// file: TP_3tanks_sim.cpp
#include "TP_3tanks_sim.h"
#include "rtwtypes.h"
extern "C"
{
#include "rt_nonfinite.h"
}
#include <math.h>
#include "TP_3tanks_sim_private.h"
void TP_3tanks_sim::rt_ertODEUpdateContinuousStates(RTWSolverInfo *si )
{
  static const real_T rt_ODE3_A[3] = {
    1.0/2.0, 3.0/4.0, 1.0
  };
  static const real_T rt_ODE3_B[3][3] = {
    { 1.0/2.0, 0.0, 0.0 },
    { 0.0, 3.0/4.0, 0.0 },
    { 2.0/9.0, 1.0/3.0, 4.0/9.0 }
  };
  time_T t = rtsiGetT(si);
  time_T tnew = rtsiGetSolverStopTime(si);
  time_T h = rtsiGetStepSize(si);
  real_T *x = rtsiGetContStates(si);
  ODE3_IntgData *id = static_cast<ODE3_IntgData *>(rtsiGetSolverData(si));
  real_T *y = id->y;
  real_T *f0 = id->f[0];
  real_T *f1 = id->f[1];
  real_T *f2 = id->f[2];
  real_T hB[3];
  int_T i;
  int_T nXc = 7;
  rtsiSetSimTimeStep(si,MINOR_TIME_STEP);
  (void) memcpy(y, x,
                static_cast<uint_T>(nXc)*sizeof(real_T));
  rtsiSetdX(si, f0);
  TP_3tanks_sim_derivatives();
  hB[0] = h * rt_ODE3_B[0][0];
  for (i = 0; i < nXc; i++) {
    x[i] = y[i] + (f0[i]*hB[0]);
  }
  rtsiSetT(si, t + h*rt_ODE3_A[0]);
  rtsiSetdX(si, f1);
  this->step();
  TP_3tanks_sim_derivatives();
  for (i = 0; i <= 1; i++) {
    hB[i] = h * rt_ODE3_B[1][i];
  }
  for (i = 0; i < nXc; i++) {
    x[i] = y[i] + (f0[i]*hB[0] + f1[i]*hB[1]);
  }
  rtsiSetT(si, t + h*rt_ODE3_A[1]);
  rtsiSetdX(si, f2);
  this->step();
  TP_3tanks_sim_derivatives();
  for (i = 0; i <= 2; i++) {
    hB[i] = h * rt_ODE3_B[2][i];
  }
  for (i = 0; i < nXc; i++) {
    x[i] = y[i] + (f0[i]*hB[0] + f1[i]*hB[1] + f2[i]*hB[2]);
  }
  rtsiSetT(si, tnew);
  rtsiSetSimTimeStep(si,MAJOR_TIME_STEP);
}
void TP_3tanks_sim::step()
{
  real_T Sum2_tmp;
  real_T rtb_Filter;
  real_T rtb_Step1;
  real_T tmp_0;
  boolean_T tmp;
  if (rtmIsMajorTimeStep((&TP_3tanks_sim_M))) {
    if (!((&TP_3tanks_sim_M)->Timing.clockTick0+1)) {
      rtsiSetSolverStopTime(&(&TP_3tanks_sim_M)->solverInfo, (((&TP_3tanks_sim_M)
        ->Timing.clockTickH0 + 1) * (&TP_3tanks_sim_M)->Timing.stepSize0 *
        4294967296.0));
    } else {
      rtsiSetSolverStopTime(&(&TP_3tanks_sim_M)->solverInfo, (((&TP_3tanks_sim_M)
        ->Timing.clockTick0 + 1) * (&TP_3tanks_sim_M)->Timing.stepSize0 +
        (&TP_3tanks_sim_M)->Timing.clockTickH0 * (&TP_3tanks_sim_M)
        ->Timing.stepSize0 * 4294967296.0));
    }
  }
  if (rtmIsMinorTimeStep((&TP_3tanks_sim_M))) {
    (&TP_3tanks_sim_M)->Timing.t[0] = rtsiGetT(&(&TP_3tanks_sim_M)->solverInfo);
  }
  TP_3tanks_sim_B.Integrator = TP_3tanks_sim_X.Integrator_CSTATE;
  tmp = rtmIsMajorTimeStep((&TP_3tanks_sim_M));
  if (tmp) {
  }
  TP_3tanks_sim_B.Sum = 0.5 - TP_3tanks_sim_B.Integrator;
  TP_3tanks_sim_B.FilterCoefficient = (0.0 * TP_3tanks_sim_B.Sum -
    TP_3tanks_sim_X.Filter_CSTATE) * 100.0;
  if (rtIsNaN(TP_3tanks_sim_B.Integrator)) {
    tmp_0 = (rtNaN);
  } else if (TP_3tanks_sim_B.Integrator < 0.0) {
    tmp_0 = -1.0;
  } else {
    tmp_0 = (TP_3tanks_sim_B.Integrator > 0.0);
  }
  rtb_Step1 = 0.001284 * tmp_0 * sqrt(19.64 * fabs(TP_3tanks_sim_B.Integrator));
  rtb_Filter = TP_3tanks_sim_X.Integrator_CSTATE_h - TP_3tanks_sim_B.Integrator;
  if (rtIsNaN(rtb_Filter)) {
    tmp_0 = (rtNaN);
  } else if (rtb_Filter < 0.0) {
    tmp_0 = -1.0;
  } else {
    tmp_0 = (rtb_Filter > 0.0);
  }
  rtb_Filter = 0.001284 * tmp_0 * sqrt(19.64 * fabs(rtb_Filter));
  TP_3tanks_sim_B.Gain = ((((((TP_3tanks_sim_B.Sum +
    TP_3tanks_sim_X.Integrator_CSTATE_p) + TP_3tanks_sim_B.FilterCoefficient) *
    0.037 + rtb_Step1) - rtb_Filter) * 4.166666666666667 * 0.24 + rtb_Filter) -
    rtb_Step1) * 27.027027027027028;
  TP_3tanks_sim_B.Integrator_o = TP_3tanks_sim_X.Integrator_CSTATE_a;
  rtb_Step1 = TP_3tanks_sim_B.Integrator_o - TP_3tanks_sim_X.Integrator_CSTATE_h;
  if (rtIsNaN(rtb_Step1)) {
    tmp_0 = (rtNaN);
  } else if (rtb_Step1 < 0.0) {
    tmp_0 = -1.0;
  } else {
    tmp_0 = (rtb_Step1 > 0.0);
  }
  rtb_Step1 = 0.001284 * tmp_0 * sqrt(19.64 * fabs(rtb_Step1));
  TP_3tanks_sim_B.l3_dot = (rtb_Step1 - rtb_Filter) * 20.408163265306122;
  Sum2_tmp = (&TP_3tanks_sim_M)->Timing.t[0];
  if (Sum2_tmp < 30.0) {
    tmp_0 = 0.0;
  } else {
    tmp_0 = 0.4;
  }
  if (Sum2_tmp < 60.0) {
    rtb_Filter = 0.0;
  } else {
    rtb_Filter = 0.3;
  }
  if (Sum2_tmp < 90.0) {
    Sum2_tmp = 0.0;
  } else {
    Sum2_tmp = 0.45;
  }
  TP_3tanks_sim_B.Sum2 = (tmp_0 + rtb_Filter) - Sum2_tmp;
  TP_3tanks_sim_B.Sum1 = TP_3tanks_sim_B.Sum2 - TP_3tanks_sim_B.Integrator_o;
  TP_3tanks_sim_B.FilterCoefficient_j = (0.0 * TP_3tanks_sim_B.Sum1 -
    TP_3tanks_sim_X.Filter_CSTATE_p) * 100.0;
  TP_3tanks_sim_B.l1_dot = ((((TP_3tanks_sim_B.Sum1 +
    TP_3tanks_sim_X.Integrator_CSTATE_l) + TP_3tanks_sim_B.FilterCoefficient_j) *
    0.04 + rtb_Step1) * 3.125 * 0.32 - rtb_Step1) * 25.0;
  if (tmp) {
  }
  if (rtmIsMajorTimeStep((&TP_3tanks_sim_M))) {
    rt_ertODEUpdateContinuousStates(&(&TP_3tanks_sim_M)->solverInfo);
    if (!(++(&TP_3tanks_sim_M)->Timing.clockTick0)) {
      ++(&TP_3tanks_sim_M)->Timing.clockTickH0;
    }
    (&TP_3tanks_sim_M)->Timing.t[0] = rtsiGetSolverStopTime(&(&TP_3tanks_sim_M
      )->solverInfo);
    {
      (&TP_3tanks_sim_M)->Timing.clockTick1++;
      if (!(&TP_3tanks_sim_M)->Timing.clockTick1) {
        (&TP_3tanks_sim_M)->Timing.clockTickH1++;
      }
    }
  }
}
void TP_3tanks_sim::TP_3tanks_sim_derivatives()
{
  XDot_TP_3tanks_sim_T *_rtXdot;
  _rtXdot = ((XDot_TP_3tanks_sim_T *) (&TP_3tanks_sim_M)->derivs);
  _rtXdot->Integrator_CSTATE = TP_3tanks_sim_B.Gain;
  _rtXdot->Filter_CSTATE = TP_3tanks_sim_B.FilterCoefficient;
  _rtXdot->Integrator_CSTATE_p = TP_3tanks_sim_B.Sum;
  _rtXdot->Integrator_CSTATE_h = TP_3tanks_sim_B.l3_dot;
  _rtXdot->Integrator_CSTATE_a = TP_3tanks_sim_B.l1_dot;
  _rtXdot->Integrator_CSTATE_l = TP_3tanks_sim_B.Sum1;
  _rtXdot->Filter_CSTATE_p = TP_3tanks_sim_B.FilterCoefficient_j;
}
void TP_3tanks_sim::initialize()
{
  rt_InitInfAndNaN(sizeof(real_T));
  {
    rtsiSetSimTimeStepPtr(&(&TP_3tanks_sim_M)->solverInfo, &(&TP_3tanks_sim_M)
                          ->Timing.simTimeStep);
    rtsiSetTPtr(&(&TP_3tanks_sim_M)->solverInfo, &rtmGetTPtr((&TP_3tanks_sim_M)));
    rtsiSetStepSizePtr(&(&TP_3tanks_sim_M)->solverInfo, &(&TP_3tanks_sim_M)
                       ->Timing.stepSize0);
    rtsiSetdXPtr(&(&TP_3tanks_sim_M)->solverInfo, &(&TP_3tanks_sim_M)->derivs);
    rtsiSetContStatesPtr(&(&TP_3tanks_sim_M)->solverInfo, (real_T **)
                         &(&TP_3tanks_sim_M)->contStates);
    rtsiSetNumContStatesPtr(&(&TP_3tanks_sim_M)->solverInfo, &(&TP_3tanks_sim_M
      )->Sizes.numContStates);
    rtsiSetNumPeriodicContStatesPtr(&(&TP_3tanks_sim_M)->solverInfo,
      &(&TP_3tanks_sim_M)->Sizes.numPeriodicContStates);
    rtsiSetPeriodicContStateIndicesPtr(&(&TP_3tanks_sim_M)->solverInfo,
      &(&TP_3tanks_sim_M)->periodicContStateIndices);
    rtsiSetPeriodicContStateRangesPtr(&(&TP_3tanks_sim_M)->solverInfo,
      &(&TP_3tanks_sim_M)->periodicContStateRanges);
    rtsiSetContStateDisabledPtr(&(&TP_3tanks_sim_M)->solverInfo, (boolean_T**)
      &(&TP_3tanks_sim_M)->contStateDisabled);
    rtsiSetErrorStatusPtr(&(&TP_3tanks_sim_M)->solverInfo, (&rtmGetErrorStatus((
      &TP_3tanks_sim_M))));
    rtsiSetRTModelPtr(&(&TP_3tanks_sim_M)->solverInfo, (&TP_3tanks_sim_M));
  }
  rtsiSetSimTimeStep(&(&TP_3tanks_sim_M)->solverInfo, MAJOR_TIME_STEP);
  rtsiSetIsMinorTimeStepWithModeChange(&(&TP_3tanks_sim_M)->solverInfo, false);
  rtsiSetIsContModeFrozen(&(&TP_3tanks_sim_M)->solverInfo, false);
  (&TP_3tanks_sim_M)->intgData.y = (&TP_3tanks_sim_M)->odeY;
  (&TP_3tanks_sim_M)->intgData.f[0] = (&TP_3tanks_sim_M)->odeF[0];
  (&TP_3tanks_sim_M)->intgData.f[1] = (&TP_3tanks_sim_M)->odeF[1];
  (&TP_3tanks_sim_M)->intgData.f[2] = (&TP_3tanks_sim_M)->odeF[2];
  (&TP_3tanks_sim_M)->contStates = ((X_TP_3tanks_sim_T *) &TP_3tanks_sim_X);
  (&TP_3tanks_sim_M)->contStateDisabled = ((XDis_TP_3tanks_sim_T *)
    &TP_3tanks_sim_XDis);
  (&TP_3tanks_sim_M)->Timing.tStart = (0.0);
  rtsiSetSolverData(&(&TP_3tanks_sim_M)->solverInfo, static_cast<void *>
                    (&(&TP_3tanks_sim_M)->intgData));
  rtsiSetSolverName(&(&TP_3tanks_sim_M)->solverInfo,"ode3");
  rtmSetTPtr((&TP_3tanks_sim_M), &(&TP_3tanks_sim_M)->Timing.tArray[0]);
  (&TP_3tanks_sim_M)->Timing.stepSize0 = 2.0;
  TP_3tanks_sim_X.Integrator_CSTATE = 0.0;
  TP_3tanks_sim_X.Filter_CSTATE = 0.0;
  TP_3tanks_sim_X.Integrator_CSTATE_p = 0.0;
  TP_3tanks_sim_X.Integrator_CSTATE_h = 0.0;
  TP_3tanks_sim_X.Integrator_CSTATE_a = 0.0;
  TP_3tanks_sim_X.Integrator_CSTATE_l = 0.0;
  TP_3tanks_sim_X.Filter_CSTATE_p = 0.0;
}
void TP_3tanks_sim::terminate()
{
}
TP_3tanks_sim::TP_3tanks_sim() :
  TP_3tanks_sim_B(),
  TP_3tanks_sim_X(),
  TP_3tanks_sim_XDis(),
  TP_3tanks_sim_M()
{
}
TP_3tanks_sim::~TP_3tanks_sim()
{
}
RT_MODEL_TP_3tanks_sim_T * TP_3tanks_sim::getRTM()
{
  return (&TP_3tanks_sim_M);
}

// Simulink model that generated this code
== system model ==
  Integrator : Integrator  <- 1: Gain
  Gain : Gain  Gain=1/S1  <- 1: Sum
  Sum : Sum  Inputs=+-  <- 1: Product#1, 2: Product#2
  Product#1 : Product  <- 1: Gain#1, 2: Constant#1
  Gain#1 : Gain  Gain=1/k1  <- 1: Sum#1
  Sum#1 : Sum  Inputs=++  <- 1: Product#2, 2: Gain#2
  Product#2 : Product  <- 1: Gain#3, 2: Sqrt#1
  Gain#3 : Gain  Gain=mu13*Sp  <- 1: Signum#1
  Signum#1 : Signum  <- 1: Sum#2
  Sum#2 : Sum  Inputs=+-  <- 1: Integrator, 2: Integrator#1
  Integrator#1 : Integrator  <- 1: Gain#4
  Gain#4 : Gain  Gain=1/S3  <- 1: Sum#3
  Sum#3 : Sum  Inputs=+-  <- 1: Product#2, 2: Product#3
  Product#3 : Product  <- 1: Gain#5, 2: Sqrt#2
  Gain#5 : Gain  Gain=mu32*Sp  <- 1: Signum#2
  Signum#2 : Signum  <- 1: Sum#4
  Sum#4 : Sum  Inputs=+-  <- 1: Integrator#1, 2: Integrator#2
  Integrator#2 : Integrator  <- 1: Gain#6
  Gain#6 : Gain  Gain=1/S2  <- 1: Sum#5
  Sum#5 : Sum  Inputs=++-  <- 1: Product#4, 2: Product#3, 3: Product#5
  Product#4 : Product  <- 1: Gain#7, 2: Constant#2
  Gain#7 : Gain  Gain=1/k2  <- 1: Sum#6
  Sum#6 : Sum  Inputs=++-  <- 1: Product#5, 2: Gain#8, 3: Product#3
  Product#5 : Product  <- 1: Gain#9, 2: Sqrt#3
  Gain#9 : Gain  Gain=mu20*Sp  <- 1: Signum#3
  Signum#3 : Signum  <- 1: Integrator#2
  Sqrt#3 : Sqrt  <- 1: Gain#10
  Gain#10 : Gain  Gain=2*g  <- 1: Abs#1
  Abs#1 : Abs  <- 1: Integrator#2
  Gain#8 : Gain  Gain=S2  <- 1: PIDController#1
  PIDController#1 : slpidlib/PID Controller  Controller=PID  Form=Parallel  TimeDomain=Continuous-time  IntegratorMethod=Forward Euler  P=1  I=1  D=0  N=100  InitialConditionForIntegrator=0  ExternalReset=none  LimitOutput=off  UpperSaturationLimit=inf  LowerSaturationLimit=-inf  <- 1: Sum#7
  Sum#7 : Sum  Inputs=+-  <- 1: Constant#3, 2: Integrator#2
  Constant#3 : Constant  Value=0.5
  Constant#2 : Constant  Value=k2
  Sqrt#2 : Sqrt  <- 1: Gain#11
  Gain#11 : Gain  Gain=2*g  <- 1: Abs#2
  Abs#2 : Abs  <- 1: Sum#4
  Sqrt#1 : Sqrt  <- 1: Gain#12
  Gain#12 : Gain  Gain=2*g  <- 1: Abs#3
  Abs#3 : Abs  <- 1: Sum#2
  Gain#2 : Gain  Gain=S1  <- 1: PIDController#2
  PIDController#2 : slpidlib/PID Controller  Controller=PID  Form=Parallel  TimeDomain=Continuous-time  IntegratorMethod=Forward Euler  P=1  I=1  D=0  N=100  InitialConditionForIntegrator=0  ExternalReset=none  LimitOutput=off  UpperSaturationLimit=inf  LowerSaturationLimit=-inf  <- 1: Sum1
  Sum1 : Sum  Inputs=+-  <- 1: Sum2, 2: Integrator
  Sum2 : Sum  Inputs=++-  <- 1: Step#1, 2: Step1, 3: Step#2
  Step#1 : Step  Time=30  After=0.4
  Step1 : Step  Time=60  After=0.3
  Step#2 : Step  Time=90  After=0.45
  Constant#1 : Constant  Value=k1
